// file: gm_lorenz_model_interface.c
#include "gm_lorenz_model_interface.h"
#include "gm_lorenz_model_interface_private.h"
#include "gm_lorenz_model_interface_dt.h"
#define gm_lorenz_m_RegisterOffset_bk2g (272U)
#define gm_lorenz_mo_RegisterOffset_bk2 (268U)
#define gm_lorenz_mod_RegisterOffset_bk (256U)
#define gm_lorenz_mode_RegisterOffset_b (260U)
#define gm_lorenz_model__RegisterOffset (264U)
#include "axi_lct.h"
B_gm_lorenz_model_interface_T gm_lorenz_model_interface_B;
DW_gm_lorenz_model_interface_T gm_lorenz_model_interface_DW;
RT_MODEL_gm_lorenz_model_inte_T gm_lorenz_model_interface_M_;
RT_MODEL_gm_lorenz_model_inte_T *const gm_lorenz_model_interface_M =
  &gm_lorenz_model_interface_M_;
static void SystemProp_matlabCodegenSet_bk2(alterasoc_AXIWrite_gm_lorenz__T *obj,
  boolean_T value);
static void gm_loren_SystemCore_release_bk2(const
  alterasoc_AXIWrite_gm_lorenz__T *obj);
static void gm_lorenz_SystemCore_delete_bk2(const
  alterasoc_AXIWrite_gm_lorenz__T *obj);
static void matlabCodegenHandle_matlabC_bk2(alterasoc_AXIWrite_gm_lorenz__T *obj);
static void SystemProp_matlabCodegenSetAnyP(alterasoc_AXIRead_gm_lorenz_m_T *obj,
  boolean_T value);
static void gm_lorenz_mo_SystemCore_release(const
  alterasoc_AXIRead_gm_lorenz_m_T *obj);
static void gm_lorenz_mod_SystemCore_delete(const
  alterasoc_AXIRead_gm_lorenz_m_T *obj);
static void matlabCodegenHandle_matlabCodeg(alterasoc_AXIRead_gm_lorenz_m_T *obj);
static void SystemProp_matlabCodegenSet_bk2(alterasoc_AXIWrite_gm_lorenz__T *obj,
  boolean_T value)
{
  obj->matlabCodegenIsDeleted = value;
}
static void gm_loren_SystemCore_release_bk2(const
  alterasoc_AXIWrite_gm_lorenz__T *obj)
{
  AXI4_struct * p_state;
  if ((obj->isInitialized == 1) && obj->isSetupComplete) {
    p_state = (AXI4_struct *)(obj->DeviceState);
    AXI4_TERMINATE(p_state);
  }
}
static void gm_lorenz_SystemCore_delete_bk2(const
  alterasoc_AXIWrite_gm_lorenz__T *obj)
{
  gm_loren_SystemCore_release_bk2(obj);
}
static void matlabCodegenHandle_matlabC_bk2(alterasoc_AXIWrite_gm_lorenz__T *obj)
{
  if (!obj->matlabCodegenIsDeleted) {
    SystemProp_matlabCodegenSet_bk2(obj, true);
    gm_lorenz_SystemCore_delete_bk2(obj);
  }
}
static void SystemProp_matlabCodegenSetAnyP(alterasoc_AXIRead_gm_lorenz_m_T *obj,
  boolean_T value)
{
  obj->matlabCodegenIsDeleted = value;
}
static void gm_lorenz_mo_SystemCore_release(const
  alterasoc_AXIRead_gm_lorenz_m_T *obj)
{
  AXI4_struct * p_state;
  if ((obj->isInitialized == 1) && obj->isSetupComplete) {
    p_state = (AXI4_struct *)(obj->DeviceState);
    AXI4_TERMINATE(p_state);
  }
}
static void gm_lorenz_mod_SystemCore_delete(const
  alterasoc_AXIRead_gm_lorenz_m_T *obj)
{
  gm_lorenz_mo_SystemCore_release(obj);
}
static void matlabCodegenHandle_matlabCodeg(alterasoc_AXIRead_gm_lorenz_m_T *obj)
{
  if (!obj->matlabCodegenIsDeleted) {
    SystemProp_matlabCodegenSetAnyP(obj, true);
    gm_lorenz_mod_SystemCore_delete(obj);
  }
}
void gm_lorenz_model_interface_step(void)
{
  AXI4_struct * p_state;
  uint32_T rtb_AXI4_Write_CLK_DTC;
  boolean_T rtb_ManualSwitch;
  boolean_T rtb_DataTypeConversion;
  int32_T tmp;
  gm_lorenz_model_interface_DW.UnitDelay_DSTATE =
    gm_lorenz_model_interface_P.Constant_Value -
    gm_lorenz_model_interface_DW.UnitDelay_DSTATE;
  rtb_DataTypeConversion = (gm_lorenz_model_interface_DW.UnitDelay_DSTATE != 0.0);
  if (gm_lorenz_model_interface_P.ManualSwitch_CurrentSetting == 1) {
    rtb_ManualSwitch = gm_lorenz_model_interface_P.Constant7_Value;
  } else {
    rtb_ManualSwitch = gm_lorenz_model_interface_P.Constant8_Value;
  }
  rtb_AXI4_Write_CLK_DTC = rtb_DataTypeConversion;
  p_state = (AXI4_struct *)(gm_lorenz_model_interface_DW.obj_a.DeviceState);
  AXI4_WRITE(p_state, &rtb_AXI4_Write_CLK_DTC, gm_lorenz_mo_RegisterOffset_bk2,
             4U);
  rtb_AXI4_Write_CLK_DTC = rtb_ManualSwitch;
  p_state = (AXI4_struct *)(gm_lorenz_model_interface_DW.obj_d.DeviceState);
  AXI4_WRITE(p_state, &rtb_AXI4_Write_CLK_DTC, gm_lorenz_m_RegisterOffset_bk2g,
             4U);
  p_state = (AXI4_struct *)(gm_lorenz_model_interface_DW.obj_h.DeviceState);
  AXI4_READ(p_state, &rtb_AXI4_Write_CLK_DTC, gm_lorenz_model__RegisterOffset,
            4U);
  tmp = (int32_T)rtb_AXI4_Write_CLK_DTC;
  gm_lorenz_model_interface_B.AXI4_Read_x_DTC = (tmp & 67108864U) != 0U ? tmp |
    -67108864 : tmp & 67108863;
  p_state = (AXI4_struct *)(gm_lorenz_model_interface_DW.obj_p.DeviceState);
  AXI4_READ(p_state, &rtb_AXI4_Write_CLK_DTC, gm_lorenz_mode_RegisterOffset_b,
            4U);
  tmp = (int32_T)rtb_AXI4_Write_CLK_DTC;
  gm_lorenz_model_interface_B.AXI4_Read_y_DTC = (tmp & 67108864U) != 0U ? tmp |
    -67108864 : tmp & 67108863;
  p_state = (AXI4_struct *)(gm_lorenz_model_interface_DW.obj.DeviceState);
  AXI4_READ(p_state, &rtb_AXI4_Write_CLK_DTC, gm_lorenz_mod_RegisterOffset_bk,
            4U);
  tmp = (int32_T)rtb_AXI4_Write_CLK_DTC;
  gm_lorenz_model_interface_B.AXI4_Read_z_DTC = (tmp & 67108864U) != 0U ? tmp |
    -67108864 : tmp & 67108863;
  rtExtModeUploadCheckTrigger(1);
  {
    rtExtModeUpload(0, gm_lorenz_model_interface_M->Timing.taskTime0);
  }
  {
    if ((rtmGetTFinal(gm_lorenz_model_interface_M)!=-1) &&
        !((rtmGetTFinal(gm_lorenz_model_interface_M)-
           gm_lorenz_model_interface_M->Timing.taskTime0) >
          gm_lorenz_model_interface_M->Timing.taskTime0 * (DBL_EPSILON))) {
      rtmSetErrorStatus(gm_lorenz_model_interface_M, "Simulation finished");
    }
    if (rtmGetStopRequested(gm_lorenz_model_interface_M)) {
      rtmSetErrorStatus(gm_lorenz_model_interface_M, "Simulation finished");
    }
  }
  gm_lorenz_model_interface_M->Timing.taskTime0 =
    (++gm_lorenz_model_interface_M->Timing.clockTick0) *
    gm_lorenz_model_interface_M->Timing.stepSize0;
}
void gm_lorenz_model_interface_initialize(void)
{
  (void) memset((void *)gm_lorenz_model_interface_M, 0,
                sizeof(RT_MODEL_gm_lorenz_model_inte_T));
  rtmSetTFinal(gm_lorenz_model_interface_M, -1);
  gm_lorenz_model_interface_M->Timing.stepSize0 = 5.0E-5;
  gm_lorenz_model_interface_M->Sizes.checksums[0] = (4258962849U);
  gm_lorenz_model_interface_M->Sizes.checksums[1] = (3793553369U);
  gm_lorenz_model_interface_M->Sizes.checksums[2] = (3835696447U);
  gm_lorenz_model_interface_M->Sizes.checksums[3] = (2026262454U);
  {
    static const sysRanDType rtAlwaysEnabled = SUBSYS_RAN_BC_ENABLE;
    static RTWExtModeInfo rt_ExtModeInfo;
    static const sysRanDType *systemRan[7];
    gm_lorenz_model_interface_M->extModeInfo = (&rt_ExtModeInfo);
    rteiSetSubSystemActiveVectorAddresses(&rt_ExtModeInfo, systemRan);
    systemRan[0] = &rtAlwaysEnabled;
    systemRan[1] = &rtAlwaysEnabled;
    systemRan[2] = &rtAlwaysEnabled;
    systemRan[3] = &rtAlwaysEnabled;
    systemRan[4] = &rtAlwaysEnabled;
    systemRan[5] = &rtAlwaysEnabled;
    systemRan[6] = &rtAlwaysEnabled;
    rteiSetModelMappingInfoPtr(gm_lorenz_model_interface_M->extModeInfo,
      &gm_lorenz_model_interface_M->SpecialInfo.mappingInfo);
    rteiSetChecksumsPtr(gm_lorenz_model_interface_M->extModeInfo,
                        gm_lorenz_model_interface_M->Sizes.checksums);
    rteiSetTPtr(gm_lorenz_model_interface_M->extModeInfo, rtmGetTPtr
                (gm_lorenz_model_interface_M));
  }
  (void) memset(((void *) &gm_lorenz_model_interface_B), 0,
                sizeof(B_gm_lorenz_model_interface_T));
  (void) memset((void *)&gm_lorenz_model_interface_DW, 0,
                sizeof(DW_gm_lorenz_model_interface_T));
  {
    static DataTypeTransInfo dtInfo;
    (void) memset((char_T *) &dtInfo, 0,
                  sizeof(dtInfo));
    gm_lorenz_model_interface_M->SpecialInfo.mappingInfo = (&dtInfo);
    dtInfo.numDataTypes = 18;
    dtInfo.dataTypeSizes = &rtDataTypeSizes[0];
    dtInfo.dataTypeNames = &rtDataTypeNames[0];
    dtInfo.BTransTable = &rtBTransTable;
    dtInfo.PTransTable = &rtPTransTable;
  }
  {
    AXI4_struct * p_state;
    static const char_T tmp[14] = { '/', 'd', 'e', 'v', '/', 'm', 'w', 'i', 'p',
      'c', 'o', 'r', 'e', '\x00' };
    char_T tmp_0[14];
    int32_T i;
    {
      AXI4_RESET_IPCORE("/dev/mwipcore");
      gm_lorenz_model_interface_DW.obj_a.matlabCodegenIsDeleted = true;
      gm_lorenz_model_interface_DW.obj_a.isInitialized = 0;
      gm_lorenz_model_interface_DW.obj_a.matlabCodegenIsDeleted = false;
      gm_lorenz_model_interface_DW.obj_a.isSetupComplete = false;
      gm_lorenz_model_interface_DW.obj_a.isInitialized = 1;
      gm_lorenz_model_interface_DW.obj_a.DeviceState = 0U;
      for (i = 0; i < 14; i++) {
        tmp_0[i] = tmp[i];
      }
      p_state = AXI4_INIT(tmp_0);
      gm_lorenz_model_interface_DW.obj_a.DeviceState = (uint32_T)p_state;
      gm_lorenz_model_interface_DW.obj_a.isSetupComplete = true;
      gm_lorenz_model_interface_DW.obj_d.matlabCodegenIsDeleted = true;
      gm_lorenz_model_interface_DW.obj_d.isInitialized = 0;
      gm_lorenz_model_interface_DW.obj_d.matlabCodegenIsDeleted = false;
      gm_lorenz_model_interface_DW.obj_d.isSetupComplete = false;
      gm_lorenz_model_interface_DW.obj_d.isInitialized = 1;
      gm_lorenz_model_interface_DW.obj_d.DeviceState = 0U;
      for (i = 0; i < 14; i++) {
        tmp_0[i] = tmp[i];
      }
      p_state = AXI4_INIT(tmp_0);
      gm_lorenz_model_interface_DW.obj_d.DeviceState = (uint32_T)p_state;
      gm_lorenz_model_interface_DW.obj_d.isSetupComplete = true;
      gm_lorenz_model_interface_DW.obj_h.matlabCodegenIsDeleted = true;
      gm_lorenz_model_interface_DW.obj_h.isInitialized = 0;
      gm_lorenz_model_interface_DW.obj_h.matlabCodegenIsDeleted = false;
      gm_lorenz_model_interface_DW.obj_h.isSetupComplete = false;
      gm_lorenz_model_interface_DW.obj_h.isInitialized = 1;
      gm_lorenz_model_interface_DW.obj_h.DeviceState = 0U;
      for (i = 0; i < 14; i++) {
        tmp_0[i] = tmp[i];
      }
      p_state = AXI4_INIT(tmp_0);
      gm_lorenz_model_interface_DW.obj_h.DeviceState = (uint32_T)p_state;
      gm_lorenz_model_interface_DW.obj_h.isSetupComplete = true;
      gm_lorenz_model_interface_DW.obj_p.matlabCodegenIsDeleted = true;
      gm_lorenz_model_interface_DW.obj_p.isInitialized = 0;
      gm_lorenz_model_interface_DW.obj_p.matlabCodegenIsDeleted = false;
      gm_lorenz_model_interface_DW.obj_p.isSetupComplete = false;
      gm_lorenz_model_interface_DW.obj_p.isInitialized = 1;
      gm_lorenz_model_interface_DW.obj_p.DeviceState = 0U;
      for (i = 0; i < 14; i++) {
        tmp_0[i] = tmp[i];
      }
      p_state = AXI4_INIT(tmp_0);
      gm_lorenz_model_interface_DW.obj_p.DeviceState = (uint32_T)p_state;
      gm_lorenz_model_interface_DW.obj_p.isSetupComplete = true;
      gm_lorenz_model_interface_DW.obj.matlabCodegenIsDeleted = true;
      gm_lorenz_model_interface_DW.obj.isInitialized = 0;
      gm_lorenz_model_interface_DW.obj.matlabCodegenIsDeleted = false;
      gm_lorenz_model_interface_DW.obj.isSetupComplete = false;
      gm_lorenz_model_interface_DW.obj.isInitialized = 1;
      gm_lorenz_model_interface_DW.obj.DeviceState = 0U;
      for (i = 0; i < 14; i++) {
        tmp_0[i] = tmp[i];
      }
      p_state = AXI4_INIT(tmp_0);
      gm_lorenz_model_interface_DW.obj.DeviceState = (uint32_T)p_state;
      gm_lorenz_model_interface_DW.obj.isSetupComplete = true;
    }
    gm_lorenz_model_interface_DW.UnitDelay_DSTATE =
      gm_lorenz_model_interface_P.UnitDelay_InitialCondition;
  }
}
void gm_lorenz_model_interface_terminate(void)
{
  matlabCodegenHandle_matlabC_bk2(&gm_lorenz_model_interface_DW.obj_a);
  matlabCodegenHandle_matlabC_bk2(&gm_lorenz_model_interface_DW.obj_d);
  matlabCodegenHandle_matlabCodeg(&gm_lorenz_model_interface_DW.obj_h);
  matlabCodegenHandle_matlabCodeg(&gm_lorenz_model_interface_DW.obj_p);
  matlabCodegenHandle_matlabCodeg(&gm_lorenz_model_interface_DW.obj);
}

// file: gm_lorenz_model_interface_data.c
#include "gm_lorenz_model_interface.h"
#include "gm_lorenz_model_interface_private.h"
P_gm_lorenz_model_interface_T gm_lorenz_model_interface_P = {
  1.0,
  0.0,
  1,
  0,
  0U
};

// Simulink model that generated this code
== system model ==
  AXI4_Write_CLK : alterasoclib/AXI4 Write  <- 1: AXI4_Write_CLK_DTC
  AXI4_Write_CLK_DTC : DataTypeConversion  <- 1: DataTypeConversion
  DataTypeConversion : DataTypeConversion  <- 1: Clock#1
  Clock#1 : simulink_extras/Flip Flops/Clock
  AXI4Write#1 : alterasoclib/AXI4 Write  <- 1: DataTypeConversion#1
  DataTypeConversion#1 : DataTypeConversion  <- 1: ManualSwitch
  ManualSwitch : ManualSwitch  <- 1: Constant7, 2: Constant8
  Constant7 : Constant
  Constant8 : Constant  Value=0
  AXI4_Read_x_DTC : DataTypeConversion  <- 1: AXI4_Read_x
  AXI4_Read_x : alterasoclib/AXI4 Read
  AXI4_Read_y_DTC : DataTypeConversion  <- 1: AXI4_Read_y
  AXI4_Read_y : alterasoclib/AXI4 Read
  AXI4_Read_z_DTC : DataTypeConversion  <- 1: AXI4_Read_z
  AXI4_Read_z : alterasoclib/AXI4 Read
